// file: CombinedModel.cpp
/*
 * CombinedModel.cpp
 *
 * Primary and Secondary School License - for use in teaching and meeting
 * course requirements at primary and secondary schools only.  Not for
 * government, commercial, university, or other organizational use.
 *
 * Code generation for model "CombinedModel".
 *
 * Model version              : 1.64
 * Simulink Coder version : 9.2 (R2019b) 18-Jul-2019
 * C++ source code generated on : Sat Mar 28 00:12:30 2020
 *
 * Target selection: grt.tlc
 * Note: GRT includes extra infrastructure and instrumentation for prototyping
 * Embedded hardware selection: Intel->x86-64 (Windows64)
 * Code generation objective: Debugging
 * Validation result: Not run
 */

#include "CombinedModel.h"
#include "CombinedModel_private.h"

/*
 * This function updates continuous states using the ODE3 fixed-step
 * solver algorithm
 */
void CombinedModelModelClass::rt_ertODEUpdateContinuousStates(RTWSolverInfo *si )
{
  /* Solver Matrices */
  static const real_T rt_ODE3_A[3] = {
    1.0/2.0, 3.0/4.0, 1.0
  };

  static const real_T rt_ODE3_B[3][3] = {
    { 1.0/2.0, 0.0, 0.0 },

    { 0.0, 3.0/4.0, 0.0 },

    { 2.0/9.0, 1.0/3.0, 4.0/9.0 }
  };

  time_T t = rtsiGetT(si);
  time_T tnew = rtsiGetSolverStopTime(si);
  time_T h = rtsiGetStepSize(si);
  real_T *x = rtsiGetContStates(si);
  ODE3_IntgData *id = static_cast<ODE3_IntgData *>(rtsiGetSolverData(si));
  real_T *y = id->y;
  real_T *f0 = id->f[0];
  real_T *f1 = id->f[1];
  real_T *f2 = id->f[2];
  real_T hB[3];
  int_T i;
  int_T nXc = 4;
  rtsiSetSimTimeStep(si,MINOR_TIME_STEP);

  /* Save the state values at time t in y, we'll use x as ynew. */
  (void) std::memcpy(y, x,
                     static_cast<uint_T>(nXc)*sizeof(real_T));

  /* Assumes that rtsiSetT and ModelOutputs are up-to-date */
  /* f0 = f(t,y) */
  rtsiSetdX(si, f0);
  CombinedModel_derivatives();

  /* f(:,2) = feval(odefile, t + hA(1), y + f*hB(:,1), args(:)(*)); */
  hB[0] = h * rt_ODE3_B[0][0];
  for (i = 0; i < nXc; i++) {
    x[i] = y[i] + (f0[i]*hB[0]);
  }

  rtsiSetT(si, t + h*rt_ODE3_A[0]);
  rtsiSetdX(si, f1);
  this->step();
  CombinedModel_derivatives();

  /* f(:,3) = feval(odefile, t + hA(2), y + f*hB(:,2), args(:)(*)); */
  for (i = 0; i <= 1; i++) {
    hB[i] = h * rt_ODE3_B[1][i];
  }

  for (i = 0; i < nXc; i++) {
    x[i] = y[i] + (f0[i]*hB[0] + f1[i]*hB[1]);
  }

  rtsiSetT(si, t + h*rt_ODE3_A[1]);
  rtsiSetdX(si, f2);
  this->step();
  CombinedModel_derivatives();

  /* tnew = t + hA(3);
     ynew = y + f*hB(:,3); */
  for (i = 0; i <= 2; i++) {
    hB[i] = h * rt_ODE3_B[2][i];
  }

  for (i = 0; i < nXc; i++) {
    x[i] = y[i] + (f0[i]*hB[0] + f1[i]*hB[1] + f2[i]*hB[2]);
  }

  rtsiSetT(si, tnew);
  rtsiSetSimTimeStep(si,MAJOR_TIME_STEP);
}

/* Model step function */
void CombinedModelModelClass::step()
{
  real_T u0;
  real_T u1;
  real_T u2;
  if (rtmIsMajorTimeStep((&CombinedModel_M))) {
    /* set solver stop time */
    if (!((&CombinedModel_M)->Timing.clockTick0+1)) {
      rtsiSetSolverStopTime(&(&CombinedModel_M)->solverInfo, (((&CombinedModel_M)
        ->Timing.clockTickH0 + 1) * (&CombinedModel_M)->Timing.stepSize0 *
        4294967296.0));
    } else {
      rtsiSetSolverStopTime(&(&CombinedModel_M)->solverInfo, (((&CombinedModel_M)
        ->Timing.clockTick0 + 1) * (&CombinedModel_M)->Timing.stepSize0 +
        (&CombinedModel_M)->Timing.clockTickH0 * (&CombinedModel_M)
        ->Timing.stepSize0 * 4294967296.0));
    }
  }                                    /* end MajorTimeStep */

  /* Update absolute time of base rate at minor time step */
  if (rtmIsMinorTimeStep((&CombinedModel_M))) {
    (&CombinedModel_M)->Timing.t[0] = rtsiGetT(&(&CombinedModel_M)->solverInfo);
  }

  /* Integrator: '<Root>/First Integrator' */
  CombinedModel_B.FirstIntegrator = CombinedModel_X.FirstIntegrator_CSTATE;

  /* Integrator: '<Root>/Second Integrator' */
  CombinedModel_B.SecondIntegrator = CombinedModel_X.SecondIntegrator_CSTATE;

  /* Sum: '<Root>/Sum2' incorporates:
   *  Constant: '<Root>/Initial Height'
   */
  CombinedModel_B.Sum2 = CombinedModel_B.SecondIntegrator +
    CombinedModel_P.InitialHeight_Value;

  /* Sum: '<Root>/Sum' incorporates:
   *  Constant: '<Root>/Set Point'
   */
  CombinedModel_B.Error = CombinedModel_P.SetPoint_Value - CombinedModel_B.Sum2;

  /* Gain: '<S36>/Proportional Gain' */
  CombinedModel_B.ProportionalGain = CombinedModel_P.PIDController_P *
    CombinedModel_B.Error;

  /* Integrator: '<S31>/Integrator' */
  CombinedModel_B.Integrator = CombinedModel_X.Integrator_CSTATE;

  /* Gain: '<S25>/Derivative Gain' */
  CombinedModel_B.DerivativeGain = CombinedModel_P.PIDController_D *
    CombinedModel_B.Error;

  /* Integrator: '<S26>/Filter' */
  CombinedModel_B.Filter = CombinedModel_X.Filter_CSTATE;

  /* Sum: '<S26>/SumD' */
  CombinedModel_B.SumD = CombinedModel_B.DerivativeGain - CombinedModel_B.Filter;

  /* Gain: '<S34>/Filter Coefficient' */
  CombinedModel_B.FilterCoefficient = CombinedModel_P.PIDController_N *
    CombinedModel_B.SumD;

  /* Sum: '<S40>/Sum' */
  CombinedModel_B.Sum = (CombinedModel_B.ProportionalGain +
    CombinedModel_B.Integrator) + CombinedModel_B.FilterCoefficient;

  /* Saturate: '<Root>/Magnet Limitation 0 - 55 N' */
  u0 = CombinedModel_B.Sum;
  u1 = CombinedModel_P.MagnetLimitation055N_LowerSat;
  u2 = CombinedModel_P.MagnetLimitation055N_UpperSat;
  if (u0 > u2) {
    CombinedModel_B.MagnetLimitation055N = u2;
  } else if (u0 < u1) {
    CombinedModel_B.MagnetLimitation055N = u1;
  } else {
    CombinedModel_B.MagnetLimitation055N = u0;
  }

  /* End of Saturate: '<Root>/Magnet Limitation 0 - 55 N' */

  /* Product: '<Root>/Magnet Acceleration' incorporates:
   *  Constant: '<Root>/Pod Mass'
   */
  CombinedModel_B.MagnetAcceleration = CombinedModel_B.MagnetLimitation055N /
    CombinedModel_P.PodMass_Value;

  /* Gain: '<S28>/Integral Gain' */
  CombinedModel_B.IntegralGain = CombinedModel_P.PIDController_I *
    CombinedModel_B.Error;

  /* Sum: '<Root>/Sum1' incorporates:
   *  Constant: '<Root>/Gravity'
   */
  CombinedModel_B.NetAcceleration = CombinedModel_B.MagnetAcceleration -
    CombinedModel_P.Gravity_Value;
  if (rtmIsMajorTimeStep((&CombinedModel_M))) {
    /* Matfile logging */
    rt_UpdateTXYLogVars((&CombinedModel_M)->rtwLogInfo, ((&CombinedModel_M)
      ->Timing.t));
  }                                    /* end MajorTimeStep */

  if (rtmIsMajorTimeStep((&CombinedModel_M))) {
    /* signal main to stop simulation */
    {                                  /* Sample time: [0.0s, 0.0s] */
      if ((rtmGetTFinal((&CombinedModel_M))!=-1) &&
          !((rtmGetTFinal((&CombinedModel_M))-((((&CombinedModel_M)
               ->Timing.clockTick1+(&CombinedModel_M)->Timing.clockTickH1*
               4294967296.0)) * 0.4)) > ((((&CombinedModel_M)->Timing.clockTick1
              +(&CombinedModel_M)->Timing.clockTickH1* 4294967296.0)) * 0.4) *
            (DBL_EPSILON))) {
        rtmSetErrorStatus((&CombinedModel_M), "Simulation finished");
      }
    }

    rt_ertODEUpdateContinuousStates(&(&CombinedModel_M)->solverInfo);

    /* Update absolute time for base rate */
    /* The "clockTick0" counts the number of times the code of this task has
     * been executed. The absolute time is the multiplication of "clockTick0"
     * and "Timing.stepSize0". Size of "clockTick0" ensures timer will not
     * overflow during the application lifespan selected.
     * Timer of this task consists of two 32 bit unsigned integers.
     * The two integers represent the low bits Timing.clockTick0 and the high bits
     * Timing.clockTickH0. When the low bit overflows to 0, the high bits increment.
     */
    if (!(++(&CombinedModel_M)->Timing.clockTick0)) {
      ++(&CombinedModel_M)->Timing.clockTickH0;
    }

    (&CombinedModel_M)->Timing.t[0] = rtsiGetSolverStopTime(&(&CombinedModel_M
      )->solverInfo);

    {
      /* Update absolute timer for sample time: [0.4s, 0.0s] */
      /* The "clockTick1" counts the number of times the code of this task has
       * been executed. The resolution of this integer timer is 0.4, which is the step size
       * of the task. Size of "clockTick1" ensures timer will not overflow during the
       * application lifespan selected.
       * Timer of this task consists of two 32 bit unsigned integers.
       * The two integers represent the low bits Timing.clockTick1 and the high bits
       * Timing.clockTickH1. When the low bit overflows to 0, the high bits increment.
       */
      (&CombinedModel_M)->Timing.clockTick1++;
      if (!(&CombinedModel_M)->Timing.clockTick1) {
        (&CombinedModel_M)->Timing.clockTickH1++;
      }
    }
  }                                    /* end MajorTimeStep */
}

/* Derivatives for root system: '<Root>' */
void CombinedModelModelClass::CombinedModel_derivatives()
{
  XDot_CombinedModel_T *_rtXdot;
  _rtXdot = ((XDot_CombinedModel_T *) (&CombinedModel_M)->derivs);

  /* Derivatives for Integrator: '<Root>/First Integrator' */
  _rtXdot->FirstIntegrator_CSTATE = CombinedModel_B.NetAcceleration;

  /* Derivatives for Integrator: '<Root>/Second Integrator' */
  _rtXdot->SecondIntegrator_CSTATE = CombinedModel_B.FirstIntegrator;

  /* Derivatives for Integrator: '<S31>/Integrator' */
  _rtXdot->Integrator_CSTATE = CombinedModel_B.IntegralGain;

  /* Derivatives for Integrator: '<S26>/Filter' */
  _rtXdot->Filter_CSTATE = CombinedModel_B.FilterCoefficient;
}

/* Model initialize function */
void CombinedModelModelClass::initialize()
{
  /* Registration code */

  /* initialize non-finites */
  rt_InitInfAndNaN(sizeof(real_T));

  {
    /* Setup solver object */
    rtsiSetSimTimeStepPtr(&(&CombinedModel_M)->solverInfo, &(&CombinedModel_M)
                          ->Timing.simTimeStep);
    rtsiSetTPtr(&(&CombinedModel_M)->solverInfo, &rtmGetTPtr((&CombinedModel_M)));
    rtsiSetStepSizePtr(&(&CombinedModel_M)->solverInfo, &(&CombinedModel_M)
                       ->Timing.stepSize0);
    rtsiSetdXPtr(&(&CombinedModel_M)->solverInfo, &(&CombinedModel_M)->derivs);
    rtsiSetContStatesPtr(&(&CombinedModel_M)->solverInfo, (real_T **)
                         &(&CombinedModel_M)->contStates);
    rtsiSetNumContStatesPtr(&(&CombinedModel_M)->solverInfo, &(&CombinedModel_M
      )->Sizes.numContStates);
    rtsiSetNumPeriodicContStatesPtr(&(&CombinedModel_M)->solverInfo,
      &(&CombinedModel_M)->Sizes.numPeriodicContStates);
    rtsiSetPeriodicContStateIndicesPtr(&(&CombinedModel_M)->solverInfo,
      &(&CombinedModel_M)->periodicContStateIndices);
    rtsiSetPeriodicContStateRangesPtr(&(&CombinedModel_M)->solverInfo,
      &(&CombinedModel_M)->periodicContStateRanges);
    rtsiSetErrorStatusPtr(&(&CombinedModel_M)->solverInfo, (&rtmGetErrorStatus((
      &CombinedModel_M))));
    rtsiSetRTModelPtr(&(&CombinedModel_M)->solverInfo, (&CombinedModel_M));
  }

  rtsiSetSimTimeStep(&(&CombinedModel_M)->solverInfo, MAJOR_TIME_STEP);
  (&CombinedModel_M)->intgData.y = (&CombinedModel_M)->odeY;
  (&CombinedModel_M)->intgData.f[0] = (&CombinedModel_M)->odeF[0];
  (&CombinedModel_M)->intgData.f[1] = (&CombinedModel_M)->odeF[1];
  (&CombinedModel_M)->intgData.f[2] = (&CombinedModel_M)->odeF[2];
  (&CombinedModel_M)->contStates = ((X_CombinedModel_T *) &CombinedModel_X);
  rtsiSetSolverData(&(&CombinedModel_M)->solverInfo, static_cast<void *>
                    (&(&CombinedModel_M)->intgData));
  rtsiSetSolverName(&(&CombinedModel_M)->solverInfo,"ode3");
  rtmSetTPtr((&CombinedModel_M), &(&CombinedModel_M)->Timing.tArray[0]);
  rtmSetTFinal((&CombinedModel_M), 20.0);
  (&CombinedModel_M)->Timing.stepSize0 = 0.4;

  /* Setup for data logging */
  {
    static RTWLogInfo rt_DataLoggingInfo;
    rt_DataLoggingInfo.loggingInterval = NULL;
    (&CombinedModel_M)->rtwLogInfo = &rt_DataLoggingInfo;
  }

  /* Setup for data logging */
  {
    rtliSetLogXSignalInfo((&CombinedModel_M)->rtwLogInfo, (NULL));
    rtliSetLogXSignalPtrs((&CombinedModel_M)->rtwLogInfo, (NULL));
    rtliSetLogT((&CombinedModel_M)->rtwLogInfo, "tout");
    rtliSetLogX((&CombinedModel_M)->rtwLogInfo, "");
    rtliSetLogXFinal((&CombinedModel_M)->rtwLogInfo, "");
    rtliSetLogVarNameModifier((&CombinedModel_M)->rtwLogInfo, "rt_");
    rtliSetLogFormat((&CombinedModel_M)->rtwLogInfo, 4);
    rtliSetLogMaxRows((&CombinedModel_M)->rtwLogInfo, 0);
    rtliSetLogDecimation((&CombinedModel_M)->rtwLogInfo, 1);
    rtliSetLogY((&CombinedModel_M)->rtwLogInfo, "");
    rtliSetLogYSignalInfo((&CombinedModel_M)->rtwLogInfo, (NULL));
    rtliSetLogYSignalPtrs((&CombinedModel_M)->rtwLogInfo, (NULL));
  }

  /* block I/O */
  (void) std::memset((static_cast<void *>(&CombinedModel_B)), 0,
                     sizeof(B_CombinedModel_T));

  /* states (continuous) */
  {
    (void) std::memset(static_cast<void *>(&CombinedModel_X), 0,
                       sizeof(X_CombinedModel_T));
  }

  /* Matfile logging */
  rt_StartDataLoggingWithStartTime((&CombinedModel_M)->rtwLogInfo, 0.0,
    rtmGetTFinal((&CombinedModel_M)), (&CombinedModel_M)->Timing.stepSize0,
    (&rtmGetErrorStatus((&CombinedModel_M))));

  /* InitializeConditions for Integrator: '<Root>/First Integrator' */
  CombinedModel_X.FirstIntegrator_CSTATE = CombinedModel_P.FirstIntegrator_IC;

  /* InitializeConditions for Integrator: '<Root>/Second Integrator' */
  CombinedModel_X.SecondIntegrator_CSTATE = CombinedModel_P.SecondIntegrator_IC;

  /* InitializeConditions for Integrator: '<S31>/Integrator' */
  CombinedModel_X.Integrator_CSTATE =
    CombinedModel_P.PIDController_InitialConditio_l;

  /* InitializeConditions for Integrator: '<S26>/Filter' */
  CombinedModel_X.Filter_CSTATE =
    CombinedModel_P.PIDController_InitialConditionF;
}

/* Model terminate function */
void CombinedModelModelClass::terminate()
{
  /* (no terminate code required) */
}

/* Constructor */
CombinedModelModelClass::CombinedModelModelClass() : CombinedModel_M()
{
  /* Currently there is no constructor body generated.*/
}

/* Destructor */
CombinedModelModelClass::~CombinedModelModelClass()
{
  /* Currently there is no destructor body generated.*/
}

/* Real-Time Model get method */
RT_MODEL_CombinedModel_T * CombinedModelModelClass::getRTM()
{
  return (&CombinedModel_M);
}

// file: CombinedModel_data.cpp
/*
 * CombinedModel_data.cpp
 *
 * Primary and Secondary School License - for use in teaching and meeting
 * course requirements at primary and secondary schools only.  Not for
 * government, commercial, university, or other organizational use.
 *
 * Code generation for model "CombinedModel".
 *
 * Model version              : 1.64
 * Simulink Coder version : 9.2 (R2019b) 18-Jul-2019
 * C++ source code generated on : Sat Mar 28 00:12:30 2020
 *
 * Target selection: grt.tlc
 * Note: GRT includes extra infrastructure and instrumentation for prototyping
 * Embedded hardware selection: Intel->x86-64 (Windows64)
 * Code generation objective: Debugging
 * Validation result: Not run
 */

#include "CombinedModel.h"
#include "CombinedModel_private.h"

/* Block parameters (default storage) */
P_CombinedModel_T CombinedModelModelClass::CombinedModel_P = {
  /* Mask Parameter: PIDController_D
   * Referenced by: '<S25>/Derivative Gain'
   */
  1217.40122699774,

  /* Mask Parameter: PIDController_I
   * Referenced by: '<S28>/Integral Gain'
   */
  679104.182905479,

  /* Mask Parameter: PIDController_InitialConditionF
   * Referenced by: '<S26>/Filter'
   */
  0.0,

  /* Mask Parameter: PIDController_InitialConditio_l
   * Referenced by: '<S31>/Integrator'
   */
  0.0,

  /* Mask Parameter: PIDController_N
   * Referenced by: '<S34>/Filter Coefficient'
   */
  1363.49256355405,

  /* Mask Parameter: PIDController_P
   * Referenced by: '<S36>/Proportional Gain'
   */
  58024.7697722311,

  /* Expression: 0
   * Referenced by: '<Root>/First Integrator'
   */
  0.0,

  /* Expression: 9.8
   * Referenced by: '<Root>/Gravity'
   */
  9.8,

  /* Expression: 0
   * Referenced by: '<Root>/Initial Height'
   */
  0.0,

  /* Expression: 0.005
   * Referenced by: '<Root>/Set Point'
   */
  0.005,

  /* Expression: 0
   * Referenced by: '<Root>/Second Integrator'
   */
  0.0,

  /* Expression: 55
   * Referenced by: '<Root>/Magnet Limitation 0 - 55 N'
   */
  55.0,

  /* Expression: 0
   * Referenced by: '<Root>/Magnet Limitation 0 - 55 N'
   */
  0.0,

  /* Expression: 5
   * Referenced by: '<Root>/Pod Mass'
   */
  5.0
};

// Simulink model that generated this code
simulink model "CombinedModel"  (R2019b)
settings: Solver=FixedStepAuto  StartTime=0.0  StopTime=20  RelTol=1e-3
libraries: simulink x1

== system CombinedModel ==
  note: Magnet
      |  Force
  First Integrator : Integrator
  Gravity : Constant  Value=9.8
  Initial Height : Constant  Value=0
  Magnet Acceleration : Product  Inputs=*/
  Magnet Limitation 0 - 55 N : Saturate  UpperLimit=55  LowerLimit=0
  PID Controller : simulink/Continuous/PID Controller  Controller=PID  Form=Parallel  TimeDomain=Continuous-time  SampleTime=-1  IntegratorMethod=Forward Euler  FilterMethod=Forward Euler  ControllerParametersSource=internal  P=58024.7697722311  I=679104.182905479  D=1217.40122699774  UseFilter=on  N=1363.49256355405  TunerSelectOption=Transfer Function Based (PID Tuner App)  InitialConditionSource=internal  InitialConditionForIntegrator=0  InitialConditionForFilter=0  DifferentiatorICPrevScaledInput=0  ExternalReset=none  TrackingMode=off  Kt=1  LimitOutput=off  UpperSaturationLimit=inf  LowerSaturationLimit=-inf  LinearizeAsGain=on  AntiWindupMode=none  Kb=1  POutMin=[]  POutMax=[]  IOutMin=[]  IOutMax=[]  DOutMin=[]  DOutMax=[]  NOutMin=[]  NOutMax=[]  SumOutMin=[]  SumOutMax=[]  SaturationOutMin=[]  SaturationOutMax=[]  PParamMin=[]  PParamMax=[]  IParamMin=[]  IParamMax=[]  DParamMin=[]  DParamMax=[]  NParamMin=[]  NParamMax=[]  KbParamMin=[]  KbParamMax=[]  KtParamMin=[]  KtParamMax=[]  KbOutMin=[]  KbOutMax=[]  KtOutMin=[]  KtOutMax=[]  IntegratorOutMin=[]  IntegratorOutMax=[]  FilterOutMin=[]  FilterOutMax=[]  SumI1OutMin=[]  SumI1OutMax=[]  SumI2OutMin=[]  SumI2OutMax=[]  SumI3OutMin=[]  SumI3OutMax=[]  SumI4OutMin=[]  SumI4OutMax=[]  SumDOutMin=[]  SumDOutMax=[]  DifferentiatorOutMin=[]  DifferentiatorOutMax=[]  FilterDiffOutCoefMin=[]  FilterDiffOutCoefMax=[]  ReciprocalOutMin=[]  ReciprocalOutMax=[]  SumDenOutMin=[]  SumDenOutMax=[]  SumNumOutMin=[]  SumNumOutMax=[]  DivideOutMin=[]  DivideOutMax=[]  IntegratorContinuousStateAttributes=''  IntegratorStateMustResolveToSignalObject=off  IntegratorRTWStateStorageClass=Auto  FilterContinuousStateAttributes=''  FilterStateMustResolveToSignalObject=off  FilterRTWStateStorageClass=Auto  ParallelPVariant=InternalParameters  IdealPVariant=Disabled  IVariant=InternalParameters  DVariant=InternalParameters  IntegratorVariant=Continuous  SatVariant=Disabled  AWVariant=Passthrough  PCopyVariant=Disabled  TRVariant=Disabled  FdbkBlocksVariant=Forward  IdealPFdbkVariant=Disabled  SatFdbkVariant=Disabled  DerivativeFilterVariant=ContFilter  NVariant=InternalParameters  NCopyVariant=Disabled  FilterICVariant=InternalICsFilter  IntegratorICVariant=InternalICs  ExternalResetVariant=Disabled  TRSumVariant=Passthrough  SumFdbkVariant=Disabled  SumVariant=Sum_PID
  Pod Mass : Constant  Value=5
  Second Integrator : Integrator
  Set Point : Constant  Value=0.005
  Sum : Sum  Inputs=|+-
  Sum1 : Sum  Inputs=+-|
  Sum2 : Sum  Inputs=|++
  wires:
  Set Point/1 -> Sum/1  "Set Point"
  Sum/1 -> PID Controller/1  "Error"
  Initial Height/1 -> Sum2/2
  Second Integrator/1 -> Sum2/1
  Sum1/1 -> First Integrator/1  "Net Acceleration"
  Magnet Acceleration/1 -> Sum1/1
  Gravity/1 -> Sum1/2
  Magnet Limitation 0 - 55 N/1 -> Magnet Acceleration/1
  Pod Mass/1 -> Magnet Acceleration/2
  First Integrator/1 -> Second Integrator/1
  PID Controller/1 -> Magnet Limitation 0 - 55 N/1  "PID Output"
  Sum2/1 -> Sum/2
